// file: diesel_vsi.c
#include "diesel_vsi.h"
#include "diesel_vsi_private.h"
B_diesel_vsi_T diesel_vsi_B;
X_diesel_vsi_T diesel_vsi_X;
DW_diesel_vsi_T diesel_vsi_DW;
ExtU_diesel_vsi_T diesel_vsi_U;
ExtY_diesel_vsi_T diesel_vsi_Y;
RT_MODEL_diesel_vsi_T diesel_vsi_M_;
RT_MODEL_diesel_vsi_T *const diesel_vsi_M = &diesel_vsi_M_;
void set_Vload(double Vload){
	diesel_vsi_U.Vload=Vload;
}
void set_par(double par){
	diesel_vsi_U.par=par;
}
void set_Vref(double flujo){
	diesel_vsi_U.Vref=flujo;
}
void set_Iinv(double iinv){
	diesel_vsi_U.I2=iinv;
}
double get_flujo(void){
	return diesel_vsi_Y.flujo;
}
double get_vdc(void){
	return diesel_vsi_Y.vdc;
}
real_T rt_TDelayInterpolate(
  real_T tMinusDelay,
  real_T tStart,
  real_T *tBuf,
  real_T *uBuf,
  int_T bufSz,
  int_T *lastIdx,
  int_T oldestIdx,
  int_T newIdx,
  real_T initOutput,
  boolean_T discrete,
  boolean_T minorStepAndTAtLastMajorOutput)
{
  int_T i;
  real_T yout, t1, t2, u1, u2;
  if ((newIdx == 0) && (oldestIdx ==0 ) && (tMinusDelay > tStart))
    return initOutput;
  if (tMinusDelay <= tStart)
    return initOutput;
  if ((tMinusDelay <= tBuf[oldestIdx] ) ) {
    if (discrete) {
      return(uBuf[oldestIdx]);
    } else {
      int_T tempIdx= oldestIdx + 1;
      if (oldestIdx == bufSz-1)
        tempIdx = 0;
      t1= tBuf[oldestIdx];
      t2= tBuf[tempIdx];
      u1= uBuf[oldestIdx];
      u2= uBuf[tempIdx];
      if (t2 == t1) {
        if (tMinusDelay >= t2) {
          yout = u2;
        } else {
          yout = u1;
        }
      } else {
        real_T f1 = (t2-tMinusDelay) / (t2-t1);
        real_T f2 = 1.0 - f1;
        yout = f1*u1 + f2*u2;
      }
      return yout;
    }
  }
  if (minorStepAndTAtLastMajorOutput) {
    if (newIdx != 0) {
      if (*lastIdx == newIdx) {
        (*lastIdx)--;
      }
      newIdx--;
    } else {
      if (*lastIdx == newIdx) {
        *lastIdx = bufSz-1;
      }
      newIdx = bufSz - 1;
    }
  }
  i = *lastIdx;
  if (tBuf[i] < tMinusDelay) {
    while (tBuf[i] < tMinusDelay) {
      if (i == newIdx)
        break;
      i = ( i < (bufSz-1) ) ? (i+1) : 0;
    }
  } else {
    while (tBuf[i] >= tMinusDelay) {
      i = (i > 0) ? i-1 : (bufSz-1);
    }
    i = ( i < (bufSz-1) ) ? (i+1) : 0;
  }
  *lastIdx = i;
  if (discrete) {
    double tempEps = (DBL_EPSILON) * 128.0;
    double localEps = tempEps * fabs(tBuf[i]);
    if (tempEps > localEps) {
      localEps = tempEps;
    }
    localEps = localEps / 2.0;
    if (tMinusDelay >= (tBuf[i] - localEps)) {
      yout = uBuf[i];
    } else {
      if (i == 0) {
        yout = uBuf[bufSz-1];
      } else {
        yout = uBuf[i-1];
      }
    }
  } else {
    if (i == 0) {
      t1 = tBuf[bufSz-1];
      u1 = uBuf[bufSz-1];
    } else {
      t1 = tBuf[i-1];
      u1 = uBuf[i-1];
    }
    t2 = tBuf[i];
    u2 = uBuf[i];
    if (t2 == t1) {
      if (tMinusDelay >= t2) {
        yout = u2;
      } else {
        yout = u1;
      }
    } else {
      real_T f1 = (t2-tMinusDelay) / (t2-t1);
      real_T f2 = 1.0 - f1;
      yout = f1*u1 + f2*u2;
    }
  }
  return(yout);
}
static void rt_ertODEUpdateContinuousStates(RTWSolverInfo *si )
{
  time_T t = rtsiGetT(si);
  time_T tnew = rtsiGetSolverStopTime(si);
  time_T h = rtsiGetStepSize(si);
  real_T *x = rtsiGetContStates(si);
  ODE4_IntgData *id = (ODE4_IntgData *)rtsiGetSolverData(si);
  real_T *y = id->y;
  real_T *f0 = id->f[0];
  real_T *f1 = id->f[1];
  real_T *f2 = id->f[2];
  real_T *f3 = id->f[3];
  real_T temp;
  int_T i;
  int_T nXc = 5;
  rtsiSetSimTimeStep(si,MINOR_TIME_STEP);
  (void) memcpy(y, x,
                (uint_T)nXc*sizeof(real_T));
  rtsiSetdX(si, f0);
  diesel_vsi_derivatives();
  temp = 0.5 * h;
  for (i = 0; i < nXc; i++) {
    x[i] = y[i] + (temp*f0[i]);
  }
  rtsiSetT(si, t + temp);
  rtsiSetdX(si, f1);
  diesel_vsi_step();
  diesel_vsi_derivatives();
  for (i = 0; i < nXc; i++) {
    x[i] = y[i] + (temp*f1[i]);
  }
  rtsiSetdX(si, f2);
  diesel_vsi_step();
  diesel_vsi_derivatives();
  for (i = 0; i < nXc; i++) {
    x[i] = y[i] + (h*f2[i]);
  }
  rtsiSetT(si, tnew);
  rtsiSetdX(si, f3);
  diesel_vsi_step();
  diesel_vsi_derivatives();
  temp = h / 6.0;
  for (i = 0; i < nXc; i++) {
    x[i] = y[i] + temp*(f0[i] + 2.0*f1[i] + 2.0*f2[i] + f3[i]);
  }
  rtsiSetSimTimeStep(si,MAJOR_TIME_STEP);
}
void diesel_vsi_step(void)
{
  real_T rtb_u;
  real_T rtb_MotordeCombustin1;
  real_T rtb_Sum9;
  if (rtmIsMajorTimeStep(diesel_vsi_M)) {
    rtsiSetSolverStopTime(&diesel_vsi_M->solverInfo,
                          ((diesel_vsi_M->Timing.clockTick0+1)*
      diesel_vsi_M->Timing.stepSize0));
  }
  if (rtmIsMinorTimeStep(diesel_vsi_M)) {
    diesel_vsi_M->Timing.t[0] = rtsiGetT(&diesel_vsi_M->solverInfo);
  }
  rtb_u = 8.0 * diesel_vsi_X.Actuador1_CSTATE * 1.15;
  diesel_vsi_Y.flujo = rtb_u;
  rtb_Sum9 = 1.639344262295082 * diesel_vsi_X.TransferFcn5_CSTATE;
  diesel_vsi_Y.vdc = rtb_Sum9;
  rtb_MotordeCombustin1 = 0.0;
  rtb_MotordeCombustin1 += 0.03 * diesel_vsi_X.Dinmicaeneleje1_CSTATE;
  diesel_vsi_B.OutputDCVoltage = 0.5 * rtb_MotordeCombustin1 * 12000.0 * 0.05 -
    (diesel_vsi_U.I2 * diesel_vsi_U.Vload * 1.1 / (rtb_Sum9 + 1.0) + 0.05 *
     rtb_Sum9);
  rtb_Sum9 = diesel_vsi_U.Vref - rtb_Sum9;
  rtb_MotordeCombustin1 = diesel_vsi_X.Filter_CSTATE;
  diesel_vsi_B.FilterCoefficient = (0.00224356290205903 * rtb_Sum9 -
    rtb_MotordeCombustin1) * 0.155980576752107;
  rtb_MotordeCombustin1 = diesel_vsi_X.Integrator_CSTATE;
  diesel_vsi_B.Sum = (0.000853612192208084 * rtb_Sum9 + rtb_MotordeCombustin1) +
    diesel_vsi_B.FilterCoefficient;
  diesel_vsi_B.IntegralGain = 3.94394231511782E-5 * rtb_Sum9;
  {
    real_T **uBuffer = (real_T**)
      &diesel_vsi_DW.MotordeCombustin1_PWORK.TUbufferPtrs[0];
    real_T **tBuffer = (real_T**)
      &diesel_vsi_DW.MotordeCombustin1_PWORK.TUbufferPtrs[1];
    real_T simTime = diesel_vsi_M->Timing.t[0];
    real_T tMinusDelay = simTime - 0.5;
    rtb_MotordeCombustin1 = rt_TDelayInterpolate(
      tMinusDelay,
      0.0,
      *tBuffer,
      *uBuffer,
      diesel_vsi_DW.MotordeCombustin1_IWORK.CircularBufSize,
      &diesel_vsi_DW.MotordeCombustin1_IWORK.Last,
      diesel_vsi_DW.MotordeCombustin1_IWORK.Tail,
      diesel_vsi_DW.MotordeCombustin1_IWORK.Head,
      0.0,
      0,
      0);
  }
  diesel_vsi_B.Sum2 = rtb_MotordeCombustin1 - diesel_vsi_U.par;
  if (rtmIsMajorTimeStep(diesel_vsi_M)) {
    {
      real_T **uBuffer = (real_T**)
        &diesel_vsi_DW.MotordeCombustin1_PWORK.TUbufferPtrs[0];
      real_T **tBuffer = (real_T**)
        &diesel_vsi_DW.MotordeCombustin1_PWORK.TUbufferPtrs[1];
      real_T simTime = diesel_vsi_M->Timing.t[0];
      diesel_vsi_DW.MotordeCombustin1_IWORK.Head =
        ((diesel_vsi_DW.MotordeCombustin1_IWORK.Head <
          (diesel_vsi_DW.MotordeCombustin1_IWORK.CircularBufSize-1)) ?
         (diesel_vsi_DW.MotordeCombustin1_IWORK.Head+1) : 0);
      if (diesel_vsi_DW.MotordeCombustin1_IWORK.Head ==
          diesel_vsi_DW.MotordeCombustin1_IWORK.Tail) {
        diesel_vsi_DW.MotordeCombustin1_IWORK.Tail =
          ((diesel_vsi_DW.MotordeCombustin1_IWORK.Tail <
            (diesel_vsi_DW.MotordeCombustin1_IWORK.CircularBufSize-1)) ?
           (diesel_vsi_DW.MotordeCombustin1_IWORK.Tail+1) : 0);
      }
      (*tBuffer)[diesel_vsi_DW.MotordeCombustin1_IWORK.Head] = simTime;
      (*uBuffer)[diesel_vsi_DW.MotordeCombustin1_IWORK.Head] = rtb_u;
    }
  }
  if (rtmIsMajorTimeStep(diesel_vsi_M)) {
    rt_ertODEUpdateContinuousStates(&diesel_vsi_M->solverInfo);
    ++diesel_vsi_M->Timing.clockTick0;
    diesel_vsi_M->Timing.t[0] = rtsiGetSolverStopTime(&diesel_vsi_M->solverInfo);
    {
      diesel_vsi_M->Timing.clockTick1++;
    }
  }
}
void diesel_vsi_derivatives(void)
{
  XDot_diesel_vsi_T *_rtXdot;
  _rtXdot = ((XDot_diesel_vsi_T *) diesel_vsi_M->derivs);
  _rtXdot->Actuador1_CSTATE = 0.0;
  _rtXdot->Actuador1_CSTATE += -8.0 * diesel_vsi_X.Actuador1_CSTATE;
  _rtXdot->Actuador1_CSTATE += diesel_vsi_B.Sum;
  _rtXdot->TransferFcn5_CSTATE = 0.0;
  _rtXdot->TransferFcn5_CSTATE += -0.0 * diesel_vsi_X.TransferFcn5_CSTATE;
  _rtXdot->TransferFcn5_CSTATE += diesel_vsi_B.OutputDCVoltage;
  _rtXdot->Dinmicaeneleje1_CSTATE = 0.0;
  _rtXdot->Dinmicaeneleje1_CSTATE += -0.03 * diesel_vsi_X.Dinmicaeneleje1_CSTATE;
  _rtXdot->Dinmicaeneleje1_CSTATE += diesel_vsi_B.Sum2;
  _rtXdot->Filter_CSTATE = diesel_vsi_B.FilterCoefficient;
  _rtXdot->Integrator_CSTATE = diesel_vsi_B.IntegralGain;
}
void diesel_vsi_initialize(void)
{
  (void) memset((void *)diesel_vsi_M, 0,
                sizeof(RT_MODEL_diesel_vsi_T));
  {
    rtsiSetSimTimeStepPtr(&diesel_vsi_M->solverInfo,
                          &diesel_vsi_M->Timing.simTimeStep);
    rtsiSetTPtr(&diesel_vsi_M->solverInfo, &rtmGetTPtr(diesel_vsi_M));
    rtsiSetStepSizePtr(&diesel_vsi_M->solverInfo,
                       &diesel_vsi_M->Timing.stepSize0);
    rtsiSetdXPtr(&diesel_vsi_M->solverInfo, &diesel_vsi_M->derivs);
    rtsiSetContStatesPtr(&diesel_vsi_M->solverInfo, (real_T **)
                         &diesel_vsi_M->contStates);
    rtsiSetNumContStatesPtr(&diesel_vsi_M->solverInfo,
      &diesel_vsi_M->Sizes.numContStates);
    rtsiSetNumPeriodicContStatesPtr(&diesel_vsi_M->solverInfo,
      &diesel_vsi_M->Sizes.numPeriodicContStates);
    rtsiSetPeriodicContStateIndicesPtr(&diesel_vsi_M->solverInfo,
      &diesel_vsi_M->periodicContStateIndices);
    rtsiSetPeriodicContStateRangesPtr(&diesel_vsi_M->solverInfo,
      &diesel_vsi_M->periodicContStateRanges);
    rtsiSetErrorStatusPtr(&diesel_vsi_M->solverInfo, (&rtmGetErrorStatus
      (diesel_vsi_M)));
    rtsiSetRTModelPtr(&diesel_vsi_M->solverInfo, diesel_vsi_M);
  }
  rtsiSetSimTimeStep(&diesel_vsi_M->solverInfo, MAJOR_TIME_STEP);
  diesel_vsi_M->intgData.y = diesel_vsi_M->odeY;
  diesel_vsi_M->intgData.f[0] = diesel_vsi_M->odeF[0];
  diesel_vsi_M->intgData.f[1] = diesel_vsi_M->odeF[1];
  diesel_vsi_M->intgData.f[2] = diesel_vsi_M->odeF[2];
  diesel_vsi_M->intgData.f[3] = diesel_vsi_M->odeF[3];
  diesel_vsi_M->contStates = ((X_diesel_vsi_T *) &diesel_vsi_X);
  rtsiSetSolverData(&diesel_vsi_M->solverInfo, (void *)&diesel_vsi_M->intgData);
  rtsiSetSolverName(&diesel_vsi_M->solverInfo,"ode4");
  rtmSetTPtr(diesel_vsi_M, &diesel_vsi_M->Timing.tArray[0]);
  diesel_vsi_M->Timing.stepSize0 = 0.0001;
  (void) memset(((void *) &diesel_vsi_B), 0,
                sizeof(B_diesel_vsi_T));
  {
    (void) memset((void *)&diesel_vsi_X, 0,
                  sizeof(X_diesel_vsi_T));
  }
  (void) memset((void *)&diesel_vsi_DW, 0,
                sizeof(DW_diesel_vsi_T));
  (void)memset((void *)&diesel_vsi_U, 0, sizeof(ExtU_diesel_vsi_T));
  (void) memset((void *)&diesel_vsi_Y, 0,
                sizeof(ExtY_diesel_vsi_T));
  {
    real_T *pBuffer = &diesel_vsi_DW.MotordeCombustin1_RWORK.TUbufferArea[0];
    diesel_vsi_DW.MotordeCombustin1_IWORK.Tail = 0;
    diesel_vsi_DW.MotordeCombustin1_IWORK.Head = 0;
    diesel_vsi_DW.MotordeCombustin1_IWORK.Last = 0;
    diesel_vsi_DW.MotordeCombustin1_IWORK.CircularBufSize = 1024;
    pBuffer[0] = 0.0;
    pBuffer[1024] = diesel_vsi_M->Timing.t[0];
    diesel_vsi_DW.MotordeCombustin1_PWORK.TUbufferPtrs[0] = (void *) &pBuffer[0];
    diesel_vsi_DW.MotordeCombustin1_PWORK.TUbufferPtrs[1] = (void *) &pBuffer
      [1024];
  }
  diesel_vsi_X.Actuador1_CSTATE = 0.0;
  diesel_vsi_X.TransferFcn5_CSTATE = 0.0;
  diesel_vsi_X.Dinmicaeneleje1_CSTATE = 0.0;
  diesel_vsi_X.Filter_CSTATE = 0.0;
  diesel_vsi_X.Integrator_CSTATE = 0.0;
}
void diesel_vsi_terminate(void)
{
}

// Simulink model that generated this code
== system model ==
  Vload : Inport
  Vref : Inport
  par : Inport
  I2 : Inport
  flujo : Outport  <- 1: Gain#1
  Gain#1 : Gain  Gain=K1  <- 1: Actuador1
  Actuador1 : TransferFcn  Numerator=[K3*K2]  Denominator=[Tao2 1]  <- 1: PIDController#1
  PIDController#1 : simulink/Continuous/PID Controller  Controller=PID  TimeDomain=Continuous-time  IntegratorMethod=Forward Euler  Form=Parallel  P=0.000853612192208084  I=3.94394231511782e-05  D=0.00224356290205903  N=0.155980576752107  InitialConditionForIntegrator=0  ExternalReset=none  LimitOutput=off  UpperSaturationLimit=inf  LowerSaturationLimit=-inf  <- 1: Sum9
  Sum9 : Sum  Inputs=+-  <- 1: Vref, 2: TransferFcn5
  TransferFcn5 : TransferFcn  Denominator=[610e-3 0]  <- 1: Sum#1
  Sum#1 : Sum  Inputs=+-  <- 1: Gain#2, 2: Sum#2
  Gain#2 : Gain  Gain=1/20  <- 1: Gain#3
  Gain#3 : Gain  Gain=12000  <- 1: Gain#4
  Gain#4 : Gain  Gain=1/2  <- 1: Dinmicaeneleje1
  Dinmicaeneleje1 : TransferFcn  Numerator=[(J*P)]  Denominator=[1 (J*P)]  <- 1: Sum2
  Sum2 : Sum  Inputs=+-  <- 1: MotordeCombustin1, 2: par
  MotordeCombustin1 : TransportDelay  <- 1: Gain#1
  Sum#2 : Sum  Inputs=++  <- 1: Product#1, 2: Gain#5
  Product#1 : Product  Inputs=*/  <- 1: Gain#6, 2: Sum#3
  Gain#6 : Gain  Gain=1.1  <- 1: Product#2
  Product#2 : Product  <- 1: I2, 2: Vload
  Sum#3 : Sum  Inputs=++  <- 1: TransferFcn5, 2: Constant#1
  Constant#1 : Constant
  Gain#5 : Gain  Gain=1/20  <- 1: TransferFcn5
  vdc : Outport  <- 1: TransferFcn5
